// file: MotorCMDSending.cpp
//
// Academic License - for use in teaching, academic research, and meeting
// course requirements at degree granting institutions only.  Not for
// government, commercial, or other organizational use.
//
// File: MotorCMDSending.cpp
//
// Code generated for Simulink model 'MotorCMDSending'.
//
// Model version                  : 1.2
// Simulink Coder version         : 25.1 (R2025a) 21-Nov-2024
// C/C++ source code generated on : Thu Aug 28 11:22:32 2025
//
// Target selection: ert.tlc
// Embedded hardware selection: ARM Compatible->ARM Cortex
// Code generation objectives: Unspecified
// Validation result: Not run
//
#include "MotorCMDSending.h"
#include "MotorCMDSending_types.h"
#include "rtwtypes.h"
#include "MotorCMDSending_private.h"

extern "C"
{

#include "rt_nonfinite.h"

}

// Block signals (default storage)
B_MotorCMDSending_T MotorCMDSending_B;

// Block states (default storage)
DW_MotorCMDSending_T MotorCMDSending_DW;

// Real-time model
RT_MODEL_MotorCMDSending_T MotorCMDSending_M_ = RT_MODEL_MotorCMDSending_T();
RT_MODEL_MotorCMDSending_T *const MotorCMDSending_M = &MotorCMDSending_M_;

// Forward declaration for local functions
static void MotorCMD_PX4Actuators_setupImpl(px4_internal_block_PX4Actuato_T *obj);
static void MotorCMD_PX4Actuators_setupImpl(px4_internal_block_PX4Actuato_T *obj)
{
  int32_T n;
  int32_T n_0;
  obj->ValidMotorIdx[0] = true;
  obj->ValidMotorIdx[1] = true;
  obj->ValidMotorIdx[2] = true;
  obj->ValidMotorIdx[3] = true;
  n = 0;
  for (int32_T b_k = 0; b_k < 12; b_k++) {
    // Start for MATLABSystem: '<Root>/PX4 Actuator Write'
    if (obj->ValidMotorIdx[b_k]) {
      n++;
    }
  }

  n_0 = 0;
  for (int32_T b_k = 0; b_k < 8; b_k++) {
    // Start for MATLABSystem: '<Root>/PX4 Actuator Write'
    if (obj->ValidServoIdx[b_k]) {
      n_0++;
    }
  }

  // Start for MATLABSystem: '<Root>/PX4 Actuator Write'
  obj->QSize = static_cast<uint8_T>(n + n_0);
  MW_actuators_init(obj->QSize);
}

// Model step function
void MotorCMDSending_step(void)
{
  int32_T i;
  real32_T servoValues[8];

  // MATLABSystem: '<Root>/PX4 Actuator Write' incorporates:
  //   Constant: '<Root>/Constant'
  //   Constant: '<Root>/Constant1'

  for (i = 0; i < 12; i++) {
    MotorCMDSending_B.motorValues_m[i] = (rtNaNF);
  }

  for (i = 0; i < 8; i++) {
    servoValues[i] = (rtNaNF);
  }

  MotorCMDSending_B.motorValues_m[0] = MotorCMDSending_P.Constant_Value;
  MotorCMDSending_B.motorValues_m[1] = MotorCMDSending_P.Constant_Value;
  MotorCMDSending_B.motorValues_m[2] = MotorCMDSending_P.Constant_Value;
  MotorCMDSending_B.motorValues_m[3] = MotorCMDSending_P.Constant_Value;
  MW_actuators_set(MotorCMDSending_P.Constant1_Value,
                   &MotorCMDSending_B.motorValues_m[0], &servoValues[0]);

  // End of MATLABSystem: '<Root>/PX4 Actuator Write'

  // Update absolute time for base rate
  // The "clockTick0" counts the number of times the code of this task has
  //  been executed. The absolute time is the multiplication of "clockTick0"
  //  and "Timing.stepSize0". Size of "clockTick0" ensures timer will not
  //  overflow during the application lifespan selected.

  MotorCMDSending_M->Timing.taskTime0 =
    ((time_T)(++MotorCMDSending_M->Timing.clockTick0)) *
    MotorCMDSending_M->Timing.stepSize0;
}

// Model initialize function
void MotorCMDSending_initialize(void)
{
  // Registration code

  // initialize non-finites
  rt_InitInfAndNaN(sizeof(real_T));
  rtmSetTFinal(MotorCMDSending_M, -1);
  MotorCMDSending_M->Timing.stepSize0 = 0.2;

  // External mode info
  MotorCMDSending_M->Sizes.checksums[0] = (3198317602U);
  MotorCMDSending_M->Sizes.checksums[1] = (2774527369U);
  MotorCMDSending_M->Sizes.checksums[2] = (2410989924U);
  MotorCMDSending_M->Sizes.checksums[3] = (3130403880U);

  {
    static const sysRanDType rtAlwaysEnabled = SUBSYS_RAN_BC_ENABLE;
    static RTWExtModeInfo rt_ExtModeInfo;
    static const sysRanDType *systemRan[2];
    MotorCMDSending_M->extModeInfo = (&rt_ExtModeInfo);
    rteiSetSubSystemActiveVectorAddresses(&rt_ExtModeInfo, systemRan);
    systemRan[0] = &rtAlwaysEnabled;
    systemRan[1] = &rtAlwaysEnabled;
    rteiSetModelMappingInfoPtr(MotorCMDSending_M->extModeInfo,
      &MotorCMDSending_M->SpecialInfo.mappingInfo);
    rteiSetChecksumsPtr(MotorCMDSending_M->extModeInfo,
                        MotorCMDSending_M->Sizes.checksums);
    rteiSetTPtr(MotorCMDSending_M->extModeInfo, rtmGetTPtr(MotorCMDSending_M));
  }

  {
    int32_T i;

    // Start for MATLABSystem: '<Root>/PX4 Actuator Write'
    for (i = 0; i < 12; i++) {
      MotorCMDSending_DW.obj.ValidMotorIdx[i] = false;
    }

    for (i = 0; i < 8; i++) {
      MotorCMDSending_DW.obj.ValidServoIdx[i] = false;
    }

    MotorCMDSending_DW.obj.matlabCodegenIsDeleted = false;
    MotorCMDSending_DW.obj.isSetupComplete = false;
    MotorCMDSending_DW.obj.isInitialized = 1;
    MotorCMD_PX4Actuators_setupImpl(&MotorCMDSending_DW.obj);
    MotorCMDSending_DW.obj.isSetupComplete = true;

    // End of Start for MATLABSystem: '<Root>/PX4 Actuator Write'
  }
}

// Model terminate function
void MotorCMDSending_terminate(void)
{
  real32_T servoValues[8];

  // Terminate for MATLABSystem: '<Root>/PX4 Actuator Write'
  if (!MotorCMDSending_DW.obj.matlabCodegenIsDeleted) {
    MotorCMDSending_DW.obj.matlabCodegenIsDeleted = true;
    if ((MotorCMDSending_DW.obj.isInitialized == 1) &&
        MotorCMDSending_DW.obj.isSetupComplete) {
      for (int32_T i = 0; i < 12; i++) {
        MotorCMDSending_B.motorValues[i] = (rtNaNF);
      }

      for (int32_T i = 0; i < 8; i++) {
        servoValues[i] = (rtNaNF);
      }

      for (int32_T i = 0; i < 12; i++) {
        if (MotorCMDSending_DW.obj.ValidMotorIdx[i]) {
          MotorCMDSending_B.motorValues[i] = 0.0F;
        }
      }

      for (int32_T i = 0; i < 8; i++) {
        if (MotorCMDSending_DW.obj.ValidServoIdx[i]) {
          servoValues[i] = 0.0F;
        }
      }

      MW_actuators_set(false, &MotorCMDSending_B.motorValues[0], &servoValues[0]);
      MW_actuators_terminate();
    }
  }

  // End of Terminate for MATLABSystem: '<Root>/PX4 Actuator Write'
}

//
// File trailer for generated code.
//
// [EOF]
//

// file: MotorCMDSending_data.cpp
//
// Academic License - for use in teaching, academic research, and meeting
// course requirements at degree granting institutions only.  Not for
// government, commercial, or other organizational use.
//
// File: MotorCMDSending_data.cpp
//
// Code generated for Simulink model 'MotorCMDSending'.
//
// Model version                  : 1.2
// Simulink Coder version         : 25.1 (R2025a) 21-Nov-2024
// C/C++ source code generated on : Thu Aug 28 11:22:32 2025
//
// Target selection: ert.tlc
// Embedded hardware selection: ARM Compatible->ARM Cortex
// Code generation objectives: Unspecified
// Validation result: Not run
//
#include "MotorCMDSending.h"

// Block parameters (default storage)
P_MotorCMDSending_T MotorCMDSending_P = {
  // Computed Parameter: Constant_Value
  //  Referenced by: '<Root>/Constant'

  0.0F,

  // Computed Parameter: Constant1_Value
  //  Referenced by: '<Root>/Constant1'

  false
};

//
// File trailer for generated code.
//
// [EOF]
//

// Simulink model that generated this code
simulink model "MotorCMDSending"  (R2025a)
settings: Solver=FixedStepAuto  StartTime=0.0  StopTime=inf  RelTol=1e-3  EnableMultiTasking=on
libraries: px4Peripheralslib x1

== system MotorCMDSending ==
  Constant : Constant  Value=0  OutDataTypeStr=single
  Constant1 : Constant  Value=0  OutDataTypeStr=boolean
  PX4 Actuator Write : px4Peripheralslib/PX4 Actuator Write  Motor1Enable=on  Motor2Enable=on  Motor3Enable=on  Motor4Enable=on  Motor5Enable=off  Motor6Enable=off  Motor7Enable=off  Motor8Enable=off  Motor9Enable=off  Motor10Enable=off  Motor11Enable=off  Motor12Enable=off  IsMotorArray=off  Servo1Enable=off  Servo2Enable=off  Servo3Enable=off  Servo4Enable=off  Servo5Enable=off  Servo6Enable=off  Servo7Enable=off  Servo8Enable=off  IsServoArray=off
  Slider : SliderBlock  ScaleMax=1
  Toggle Switch : ToggleSwitchBlock
  wires:
  Constant/1 -> PX4 Actuator Write/5, PX4 Actuator Write/2, PX4 Actuator Write/3, PX4 Actuator Write/4
  Constant1/1 -> PX4 Actuator Write/1
